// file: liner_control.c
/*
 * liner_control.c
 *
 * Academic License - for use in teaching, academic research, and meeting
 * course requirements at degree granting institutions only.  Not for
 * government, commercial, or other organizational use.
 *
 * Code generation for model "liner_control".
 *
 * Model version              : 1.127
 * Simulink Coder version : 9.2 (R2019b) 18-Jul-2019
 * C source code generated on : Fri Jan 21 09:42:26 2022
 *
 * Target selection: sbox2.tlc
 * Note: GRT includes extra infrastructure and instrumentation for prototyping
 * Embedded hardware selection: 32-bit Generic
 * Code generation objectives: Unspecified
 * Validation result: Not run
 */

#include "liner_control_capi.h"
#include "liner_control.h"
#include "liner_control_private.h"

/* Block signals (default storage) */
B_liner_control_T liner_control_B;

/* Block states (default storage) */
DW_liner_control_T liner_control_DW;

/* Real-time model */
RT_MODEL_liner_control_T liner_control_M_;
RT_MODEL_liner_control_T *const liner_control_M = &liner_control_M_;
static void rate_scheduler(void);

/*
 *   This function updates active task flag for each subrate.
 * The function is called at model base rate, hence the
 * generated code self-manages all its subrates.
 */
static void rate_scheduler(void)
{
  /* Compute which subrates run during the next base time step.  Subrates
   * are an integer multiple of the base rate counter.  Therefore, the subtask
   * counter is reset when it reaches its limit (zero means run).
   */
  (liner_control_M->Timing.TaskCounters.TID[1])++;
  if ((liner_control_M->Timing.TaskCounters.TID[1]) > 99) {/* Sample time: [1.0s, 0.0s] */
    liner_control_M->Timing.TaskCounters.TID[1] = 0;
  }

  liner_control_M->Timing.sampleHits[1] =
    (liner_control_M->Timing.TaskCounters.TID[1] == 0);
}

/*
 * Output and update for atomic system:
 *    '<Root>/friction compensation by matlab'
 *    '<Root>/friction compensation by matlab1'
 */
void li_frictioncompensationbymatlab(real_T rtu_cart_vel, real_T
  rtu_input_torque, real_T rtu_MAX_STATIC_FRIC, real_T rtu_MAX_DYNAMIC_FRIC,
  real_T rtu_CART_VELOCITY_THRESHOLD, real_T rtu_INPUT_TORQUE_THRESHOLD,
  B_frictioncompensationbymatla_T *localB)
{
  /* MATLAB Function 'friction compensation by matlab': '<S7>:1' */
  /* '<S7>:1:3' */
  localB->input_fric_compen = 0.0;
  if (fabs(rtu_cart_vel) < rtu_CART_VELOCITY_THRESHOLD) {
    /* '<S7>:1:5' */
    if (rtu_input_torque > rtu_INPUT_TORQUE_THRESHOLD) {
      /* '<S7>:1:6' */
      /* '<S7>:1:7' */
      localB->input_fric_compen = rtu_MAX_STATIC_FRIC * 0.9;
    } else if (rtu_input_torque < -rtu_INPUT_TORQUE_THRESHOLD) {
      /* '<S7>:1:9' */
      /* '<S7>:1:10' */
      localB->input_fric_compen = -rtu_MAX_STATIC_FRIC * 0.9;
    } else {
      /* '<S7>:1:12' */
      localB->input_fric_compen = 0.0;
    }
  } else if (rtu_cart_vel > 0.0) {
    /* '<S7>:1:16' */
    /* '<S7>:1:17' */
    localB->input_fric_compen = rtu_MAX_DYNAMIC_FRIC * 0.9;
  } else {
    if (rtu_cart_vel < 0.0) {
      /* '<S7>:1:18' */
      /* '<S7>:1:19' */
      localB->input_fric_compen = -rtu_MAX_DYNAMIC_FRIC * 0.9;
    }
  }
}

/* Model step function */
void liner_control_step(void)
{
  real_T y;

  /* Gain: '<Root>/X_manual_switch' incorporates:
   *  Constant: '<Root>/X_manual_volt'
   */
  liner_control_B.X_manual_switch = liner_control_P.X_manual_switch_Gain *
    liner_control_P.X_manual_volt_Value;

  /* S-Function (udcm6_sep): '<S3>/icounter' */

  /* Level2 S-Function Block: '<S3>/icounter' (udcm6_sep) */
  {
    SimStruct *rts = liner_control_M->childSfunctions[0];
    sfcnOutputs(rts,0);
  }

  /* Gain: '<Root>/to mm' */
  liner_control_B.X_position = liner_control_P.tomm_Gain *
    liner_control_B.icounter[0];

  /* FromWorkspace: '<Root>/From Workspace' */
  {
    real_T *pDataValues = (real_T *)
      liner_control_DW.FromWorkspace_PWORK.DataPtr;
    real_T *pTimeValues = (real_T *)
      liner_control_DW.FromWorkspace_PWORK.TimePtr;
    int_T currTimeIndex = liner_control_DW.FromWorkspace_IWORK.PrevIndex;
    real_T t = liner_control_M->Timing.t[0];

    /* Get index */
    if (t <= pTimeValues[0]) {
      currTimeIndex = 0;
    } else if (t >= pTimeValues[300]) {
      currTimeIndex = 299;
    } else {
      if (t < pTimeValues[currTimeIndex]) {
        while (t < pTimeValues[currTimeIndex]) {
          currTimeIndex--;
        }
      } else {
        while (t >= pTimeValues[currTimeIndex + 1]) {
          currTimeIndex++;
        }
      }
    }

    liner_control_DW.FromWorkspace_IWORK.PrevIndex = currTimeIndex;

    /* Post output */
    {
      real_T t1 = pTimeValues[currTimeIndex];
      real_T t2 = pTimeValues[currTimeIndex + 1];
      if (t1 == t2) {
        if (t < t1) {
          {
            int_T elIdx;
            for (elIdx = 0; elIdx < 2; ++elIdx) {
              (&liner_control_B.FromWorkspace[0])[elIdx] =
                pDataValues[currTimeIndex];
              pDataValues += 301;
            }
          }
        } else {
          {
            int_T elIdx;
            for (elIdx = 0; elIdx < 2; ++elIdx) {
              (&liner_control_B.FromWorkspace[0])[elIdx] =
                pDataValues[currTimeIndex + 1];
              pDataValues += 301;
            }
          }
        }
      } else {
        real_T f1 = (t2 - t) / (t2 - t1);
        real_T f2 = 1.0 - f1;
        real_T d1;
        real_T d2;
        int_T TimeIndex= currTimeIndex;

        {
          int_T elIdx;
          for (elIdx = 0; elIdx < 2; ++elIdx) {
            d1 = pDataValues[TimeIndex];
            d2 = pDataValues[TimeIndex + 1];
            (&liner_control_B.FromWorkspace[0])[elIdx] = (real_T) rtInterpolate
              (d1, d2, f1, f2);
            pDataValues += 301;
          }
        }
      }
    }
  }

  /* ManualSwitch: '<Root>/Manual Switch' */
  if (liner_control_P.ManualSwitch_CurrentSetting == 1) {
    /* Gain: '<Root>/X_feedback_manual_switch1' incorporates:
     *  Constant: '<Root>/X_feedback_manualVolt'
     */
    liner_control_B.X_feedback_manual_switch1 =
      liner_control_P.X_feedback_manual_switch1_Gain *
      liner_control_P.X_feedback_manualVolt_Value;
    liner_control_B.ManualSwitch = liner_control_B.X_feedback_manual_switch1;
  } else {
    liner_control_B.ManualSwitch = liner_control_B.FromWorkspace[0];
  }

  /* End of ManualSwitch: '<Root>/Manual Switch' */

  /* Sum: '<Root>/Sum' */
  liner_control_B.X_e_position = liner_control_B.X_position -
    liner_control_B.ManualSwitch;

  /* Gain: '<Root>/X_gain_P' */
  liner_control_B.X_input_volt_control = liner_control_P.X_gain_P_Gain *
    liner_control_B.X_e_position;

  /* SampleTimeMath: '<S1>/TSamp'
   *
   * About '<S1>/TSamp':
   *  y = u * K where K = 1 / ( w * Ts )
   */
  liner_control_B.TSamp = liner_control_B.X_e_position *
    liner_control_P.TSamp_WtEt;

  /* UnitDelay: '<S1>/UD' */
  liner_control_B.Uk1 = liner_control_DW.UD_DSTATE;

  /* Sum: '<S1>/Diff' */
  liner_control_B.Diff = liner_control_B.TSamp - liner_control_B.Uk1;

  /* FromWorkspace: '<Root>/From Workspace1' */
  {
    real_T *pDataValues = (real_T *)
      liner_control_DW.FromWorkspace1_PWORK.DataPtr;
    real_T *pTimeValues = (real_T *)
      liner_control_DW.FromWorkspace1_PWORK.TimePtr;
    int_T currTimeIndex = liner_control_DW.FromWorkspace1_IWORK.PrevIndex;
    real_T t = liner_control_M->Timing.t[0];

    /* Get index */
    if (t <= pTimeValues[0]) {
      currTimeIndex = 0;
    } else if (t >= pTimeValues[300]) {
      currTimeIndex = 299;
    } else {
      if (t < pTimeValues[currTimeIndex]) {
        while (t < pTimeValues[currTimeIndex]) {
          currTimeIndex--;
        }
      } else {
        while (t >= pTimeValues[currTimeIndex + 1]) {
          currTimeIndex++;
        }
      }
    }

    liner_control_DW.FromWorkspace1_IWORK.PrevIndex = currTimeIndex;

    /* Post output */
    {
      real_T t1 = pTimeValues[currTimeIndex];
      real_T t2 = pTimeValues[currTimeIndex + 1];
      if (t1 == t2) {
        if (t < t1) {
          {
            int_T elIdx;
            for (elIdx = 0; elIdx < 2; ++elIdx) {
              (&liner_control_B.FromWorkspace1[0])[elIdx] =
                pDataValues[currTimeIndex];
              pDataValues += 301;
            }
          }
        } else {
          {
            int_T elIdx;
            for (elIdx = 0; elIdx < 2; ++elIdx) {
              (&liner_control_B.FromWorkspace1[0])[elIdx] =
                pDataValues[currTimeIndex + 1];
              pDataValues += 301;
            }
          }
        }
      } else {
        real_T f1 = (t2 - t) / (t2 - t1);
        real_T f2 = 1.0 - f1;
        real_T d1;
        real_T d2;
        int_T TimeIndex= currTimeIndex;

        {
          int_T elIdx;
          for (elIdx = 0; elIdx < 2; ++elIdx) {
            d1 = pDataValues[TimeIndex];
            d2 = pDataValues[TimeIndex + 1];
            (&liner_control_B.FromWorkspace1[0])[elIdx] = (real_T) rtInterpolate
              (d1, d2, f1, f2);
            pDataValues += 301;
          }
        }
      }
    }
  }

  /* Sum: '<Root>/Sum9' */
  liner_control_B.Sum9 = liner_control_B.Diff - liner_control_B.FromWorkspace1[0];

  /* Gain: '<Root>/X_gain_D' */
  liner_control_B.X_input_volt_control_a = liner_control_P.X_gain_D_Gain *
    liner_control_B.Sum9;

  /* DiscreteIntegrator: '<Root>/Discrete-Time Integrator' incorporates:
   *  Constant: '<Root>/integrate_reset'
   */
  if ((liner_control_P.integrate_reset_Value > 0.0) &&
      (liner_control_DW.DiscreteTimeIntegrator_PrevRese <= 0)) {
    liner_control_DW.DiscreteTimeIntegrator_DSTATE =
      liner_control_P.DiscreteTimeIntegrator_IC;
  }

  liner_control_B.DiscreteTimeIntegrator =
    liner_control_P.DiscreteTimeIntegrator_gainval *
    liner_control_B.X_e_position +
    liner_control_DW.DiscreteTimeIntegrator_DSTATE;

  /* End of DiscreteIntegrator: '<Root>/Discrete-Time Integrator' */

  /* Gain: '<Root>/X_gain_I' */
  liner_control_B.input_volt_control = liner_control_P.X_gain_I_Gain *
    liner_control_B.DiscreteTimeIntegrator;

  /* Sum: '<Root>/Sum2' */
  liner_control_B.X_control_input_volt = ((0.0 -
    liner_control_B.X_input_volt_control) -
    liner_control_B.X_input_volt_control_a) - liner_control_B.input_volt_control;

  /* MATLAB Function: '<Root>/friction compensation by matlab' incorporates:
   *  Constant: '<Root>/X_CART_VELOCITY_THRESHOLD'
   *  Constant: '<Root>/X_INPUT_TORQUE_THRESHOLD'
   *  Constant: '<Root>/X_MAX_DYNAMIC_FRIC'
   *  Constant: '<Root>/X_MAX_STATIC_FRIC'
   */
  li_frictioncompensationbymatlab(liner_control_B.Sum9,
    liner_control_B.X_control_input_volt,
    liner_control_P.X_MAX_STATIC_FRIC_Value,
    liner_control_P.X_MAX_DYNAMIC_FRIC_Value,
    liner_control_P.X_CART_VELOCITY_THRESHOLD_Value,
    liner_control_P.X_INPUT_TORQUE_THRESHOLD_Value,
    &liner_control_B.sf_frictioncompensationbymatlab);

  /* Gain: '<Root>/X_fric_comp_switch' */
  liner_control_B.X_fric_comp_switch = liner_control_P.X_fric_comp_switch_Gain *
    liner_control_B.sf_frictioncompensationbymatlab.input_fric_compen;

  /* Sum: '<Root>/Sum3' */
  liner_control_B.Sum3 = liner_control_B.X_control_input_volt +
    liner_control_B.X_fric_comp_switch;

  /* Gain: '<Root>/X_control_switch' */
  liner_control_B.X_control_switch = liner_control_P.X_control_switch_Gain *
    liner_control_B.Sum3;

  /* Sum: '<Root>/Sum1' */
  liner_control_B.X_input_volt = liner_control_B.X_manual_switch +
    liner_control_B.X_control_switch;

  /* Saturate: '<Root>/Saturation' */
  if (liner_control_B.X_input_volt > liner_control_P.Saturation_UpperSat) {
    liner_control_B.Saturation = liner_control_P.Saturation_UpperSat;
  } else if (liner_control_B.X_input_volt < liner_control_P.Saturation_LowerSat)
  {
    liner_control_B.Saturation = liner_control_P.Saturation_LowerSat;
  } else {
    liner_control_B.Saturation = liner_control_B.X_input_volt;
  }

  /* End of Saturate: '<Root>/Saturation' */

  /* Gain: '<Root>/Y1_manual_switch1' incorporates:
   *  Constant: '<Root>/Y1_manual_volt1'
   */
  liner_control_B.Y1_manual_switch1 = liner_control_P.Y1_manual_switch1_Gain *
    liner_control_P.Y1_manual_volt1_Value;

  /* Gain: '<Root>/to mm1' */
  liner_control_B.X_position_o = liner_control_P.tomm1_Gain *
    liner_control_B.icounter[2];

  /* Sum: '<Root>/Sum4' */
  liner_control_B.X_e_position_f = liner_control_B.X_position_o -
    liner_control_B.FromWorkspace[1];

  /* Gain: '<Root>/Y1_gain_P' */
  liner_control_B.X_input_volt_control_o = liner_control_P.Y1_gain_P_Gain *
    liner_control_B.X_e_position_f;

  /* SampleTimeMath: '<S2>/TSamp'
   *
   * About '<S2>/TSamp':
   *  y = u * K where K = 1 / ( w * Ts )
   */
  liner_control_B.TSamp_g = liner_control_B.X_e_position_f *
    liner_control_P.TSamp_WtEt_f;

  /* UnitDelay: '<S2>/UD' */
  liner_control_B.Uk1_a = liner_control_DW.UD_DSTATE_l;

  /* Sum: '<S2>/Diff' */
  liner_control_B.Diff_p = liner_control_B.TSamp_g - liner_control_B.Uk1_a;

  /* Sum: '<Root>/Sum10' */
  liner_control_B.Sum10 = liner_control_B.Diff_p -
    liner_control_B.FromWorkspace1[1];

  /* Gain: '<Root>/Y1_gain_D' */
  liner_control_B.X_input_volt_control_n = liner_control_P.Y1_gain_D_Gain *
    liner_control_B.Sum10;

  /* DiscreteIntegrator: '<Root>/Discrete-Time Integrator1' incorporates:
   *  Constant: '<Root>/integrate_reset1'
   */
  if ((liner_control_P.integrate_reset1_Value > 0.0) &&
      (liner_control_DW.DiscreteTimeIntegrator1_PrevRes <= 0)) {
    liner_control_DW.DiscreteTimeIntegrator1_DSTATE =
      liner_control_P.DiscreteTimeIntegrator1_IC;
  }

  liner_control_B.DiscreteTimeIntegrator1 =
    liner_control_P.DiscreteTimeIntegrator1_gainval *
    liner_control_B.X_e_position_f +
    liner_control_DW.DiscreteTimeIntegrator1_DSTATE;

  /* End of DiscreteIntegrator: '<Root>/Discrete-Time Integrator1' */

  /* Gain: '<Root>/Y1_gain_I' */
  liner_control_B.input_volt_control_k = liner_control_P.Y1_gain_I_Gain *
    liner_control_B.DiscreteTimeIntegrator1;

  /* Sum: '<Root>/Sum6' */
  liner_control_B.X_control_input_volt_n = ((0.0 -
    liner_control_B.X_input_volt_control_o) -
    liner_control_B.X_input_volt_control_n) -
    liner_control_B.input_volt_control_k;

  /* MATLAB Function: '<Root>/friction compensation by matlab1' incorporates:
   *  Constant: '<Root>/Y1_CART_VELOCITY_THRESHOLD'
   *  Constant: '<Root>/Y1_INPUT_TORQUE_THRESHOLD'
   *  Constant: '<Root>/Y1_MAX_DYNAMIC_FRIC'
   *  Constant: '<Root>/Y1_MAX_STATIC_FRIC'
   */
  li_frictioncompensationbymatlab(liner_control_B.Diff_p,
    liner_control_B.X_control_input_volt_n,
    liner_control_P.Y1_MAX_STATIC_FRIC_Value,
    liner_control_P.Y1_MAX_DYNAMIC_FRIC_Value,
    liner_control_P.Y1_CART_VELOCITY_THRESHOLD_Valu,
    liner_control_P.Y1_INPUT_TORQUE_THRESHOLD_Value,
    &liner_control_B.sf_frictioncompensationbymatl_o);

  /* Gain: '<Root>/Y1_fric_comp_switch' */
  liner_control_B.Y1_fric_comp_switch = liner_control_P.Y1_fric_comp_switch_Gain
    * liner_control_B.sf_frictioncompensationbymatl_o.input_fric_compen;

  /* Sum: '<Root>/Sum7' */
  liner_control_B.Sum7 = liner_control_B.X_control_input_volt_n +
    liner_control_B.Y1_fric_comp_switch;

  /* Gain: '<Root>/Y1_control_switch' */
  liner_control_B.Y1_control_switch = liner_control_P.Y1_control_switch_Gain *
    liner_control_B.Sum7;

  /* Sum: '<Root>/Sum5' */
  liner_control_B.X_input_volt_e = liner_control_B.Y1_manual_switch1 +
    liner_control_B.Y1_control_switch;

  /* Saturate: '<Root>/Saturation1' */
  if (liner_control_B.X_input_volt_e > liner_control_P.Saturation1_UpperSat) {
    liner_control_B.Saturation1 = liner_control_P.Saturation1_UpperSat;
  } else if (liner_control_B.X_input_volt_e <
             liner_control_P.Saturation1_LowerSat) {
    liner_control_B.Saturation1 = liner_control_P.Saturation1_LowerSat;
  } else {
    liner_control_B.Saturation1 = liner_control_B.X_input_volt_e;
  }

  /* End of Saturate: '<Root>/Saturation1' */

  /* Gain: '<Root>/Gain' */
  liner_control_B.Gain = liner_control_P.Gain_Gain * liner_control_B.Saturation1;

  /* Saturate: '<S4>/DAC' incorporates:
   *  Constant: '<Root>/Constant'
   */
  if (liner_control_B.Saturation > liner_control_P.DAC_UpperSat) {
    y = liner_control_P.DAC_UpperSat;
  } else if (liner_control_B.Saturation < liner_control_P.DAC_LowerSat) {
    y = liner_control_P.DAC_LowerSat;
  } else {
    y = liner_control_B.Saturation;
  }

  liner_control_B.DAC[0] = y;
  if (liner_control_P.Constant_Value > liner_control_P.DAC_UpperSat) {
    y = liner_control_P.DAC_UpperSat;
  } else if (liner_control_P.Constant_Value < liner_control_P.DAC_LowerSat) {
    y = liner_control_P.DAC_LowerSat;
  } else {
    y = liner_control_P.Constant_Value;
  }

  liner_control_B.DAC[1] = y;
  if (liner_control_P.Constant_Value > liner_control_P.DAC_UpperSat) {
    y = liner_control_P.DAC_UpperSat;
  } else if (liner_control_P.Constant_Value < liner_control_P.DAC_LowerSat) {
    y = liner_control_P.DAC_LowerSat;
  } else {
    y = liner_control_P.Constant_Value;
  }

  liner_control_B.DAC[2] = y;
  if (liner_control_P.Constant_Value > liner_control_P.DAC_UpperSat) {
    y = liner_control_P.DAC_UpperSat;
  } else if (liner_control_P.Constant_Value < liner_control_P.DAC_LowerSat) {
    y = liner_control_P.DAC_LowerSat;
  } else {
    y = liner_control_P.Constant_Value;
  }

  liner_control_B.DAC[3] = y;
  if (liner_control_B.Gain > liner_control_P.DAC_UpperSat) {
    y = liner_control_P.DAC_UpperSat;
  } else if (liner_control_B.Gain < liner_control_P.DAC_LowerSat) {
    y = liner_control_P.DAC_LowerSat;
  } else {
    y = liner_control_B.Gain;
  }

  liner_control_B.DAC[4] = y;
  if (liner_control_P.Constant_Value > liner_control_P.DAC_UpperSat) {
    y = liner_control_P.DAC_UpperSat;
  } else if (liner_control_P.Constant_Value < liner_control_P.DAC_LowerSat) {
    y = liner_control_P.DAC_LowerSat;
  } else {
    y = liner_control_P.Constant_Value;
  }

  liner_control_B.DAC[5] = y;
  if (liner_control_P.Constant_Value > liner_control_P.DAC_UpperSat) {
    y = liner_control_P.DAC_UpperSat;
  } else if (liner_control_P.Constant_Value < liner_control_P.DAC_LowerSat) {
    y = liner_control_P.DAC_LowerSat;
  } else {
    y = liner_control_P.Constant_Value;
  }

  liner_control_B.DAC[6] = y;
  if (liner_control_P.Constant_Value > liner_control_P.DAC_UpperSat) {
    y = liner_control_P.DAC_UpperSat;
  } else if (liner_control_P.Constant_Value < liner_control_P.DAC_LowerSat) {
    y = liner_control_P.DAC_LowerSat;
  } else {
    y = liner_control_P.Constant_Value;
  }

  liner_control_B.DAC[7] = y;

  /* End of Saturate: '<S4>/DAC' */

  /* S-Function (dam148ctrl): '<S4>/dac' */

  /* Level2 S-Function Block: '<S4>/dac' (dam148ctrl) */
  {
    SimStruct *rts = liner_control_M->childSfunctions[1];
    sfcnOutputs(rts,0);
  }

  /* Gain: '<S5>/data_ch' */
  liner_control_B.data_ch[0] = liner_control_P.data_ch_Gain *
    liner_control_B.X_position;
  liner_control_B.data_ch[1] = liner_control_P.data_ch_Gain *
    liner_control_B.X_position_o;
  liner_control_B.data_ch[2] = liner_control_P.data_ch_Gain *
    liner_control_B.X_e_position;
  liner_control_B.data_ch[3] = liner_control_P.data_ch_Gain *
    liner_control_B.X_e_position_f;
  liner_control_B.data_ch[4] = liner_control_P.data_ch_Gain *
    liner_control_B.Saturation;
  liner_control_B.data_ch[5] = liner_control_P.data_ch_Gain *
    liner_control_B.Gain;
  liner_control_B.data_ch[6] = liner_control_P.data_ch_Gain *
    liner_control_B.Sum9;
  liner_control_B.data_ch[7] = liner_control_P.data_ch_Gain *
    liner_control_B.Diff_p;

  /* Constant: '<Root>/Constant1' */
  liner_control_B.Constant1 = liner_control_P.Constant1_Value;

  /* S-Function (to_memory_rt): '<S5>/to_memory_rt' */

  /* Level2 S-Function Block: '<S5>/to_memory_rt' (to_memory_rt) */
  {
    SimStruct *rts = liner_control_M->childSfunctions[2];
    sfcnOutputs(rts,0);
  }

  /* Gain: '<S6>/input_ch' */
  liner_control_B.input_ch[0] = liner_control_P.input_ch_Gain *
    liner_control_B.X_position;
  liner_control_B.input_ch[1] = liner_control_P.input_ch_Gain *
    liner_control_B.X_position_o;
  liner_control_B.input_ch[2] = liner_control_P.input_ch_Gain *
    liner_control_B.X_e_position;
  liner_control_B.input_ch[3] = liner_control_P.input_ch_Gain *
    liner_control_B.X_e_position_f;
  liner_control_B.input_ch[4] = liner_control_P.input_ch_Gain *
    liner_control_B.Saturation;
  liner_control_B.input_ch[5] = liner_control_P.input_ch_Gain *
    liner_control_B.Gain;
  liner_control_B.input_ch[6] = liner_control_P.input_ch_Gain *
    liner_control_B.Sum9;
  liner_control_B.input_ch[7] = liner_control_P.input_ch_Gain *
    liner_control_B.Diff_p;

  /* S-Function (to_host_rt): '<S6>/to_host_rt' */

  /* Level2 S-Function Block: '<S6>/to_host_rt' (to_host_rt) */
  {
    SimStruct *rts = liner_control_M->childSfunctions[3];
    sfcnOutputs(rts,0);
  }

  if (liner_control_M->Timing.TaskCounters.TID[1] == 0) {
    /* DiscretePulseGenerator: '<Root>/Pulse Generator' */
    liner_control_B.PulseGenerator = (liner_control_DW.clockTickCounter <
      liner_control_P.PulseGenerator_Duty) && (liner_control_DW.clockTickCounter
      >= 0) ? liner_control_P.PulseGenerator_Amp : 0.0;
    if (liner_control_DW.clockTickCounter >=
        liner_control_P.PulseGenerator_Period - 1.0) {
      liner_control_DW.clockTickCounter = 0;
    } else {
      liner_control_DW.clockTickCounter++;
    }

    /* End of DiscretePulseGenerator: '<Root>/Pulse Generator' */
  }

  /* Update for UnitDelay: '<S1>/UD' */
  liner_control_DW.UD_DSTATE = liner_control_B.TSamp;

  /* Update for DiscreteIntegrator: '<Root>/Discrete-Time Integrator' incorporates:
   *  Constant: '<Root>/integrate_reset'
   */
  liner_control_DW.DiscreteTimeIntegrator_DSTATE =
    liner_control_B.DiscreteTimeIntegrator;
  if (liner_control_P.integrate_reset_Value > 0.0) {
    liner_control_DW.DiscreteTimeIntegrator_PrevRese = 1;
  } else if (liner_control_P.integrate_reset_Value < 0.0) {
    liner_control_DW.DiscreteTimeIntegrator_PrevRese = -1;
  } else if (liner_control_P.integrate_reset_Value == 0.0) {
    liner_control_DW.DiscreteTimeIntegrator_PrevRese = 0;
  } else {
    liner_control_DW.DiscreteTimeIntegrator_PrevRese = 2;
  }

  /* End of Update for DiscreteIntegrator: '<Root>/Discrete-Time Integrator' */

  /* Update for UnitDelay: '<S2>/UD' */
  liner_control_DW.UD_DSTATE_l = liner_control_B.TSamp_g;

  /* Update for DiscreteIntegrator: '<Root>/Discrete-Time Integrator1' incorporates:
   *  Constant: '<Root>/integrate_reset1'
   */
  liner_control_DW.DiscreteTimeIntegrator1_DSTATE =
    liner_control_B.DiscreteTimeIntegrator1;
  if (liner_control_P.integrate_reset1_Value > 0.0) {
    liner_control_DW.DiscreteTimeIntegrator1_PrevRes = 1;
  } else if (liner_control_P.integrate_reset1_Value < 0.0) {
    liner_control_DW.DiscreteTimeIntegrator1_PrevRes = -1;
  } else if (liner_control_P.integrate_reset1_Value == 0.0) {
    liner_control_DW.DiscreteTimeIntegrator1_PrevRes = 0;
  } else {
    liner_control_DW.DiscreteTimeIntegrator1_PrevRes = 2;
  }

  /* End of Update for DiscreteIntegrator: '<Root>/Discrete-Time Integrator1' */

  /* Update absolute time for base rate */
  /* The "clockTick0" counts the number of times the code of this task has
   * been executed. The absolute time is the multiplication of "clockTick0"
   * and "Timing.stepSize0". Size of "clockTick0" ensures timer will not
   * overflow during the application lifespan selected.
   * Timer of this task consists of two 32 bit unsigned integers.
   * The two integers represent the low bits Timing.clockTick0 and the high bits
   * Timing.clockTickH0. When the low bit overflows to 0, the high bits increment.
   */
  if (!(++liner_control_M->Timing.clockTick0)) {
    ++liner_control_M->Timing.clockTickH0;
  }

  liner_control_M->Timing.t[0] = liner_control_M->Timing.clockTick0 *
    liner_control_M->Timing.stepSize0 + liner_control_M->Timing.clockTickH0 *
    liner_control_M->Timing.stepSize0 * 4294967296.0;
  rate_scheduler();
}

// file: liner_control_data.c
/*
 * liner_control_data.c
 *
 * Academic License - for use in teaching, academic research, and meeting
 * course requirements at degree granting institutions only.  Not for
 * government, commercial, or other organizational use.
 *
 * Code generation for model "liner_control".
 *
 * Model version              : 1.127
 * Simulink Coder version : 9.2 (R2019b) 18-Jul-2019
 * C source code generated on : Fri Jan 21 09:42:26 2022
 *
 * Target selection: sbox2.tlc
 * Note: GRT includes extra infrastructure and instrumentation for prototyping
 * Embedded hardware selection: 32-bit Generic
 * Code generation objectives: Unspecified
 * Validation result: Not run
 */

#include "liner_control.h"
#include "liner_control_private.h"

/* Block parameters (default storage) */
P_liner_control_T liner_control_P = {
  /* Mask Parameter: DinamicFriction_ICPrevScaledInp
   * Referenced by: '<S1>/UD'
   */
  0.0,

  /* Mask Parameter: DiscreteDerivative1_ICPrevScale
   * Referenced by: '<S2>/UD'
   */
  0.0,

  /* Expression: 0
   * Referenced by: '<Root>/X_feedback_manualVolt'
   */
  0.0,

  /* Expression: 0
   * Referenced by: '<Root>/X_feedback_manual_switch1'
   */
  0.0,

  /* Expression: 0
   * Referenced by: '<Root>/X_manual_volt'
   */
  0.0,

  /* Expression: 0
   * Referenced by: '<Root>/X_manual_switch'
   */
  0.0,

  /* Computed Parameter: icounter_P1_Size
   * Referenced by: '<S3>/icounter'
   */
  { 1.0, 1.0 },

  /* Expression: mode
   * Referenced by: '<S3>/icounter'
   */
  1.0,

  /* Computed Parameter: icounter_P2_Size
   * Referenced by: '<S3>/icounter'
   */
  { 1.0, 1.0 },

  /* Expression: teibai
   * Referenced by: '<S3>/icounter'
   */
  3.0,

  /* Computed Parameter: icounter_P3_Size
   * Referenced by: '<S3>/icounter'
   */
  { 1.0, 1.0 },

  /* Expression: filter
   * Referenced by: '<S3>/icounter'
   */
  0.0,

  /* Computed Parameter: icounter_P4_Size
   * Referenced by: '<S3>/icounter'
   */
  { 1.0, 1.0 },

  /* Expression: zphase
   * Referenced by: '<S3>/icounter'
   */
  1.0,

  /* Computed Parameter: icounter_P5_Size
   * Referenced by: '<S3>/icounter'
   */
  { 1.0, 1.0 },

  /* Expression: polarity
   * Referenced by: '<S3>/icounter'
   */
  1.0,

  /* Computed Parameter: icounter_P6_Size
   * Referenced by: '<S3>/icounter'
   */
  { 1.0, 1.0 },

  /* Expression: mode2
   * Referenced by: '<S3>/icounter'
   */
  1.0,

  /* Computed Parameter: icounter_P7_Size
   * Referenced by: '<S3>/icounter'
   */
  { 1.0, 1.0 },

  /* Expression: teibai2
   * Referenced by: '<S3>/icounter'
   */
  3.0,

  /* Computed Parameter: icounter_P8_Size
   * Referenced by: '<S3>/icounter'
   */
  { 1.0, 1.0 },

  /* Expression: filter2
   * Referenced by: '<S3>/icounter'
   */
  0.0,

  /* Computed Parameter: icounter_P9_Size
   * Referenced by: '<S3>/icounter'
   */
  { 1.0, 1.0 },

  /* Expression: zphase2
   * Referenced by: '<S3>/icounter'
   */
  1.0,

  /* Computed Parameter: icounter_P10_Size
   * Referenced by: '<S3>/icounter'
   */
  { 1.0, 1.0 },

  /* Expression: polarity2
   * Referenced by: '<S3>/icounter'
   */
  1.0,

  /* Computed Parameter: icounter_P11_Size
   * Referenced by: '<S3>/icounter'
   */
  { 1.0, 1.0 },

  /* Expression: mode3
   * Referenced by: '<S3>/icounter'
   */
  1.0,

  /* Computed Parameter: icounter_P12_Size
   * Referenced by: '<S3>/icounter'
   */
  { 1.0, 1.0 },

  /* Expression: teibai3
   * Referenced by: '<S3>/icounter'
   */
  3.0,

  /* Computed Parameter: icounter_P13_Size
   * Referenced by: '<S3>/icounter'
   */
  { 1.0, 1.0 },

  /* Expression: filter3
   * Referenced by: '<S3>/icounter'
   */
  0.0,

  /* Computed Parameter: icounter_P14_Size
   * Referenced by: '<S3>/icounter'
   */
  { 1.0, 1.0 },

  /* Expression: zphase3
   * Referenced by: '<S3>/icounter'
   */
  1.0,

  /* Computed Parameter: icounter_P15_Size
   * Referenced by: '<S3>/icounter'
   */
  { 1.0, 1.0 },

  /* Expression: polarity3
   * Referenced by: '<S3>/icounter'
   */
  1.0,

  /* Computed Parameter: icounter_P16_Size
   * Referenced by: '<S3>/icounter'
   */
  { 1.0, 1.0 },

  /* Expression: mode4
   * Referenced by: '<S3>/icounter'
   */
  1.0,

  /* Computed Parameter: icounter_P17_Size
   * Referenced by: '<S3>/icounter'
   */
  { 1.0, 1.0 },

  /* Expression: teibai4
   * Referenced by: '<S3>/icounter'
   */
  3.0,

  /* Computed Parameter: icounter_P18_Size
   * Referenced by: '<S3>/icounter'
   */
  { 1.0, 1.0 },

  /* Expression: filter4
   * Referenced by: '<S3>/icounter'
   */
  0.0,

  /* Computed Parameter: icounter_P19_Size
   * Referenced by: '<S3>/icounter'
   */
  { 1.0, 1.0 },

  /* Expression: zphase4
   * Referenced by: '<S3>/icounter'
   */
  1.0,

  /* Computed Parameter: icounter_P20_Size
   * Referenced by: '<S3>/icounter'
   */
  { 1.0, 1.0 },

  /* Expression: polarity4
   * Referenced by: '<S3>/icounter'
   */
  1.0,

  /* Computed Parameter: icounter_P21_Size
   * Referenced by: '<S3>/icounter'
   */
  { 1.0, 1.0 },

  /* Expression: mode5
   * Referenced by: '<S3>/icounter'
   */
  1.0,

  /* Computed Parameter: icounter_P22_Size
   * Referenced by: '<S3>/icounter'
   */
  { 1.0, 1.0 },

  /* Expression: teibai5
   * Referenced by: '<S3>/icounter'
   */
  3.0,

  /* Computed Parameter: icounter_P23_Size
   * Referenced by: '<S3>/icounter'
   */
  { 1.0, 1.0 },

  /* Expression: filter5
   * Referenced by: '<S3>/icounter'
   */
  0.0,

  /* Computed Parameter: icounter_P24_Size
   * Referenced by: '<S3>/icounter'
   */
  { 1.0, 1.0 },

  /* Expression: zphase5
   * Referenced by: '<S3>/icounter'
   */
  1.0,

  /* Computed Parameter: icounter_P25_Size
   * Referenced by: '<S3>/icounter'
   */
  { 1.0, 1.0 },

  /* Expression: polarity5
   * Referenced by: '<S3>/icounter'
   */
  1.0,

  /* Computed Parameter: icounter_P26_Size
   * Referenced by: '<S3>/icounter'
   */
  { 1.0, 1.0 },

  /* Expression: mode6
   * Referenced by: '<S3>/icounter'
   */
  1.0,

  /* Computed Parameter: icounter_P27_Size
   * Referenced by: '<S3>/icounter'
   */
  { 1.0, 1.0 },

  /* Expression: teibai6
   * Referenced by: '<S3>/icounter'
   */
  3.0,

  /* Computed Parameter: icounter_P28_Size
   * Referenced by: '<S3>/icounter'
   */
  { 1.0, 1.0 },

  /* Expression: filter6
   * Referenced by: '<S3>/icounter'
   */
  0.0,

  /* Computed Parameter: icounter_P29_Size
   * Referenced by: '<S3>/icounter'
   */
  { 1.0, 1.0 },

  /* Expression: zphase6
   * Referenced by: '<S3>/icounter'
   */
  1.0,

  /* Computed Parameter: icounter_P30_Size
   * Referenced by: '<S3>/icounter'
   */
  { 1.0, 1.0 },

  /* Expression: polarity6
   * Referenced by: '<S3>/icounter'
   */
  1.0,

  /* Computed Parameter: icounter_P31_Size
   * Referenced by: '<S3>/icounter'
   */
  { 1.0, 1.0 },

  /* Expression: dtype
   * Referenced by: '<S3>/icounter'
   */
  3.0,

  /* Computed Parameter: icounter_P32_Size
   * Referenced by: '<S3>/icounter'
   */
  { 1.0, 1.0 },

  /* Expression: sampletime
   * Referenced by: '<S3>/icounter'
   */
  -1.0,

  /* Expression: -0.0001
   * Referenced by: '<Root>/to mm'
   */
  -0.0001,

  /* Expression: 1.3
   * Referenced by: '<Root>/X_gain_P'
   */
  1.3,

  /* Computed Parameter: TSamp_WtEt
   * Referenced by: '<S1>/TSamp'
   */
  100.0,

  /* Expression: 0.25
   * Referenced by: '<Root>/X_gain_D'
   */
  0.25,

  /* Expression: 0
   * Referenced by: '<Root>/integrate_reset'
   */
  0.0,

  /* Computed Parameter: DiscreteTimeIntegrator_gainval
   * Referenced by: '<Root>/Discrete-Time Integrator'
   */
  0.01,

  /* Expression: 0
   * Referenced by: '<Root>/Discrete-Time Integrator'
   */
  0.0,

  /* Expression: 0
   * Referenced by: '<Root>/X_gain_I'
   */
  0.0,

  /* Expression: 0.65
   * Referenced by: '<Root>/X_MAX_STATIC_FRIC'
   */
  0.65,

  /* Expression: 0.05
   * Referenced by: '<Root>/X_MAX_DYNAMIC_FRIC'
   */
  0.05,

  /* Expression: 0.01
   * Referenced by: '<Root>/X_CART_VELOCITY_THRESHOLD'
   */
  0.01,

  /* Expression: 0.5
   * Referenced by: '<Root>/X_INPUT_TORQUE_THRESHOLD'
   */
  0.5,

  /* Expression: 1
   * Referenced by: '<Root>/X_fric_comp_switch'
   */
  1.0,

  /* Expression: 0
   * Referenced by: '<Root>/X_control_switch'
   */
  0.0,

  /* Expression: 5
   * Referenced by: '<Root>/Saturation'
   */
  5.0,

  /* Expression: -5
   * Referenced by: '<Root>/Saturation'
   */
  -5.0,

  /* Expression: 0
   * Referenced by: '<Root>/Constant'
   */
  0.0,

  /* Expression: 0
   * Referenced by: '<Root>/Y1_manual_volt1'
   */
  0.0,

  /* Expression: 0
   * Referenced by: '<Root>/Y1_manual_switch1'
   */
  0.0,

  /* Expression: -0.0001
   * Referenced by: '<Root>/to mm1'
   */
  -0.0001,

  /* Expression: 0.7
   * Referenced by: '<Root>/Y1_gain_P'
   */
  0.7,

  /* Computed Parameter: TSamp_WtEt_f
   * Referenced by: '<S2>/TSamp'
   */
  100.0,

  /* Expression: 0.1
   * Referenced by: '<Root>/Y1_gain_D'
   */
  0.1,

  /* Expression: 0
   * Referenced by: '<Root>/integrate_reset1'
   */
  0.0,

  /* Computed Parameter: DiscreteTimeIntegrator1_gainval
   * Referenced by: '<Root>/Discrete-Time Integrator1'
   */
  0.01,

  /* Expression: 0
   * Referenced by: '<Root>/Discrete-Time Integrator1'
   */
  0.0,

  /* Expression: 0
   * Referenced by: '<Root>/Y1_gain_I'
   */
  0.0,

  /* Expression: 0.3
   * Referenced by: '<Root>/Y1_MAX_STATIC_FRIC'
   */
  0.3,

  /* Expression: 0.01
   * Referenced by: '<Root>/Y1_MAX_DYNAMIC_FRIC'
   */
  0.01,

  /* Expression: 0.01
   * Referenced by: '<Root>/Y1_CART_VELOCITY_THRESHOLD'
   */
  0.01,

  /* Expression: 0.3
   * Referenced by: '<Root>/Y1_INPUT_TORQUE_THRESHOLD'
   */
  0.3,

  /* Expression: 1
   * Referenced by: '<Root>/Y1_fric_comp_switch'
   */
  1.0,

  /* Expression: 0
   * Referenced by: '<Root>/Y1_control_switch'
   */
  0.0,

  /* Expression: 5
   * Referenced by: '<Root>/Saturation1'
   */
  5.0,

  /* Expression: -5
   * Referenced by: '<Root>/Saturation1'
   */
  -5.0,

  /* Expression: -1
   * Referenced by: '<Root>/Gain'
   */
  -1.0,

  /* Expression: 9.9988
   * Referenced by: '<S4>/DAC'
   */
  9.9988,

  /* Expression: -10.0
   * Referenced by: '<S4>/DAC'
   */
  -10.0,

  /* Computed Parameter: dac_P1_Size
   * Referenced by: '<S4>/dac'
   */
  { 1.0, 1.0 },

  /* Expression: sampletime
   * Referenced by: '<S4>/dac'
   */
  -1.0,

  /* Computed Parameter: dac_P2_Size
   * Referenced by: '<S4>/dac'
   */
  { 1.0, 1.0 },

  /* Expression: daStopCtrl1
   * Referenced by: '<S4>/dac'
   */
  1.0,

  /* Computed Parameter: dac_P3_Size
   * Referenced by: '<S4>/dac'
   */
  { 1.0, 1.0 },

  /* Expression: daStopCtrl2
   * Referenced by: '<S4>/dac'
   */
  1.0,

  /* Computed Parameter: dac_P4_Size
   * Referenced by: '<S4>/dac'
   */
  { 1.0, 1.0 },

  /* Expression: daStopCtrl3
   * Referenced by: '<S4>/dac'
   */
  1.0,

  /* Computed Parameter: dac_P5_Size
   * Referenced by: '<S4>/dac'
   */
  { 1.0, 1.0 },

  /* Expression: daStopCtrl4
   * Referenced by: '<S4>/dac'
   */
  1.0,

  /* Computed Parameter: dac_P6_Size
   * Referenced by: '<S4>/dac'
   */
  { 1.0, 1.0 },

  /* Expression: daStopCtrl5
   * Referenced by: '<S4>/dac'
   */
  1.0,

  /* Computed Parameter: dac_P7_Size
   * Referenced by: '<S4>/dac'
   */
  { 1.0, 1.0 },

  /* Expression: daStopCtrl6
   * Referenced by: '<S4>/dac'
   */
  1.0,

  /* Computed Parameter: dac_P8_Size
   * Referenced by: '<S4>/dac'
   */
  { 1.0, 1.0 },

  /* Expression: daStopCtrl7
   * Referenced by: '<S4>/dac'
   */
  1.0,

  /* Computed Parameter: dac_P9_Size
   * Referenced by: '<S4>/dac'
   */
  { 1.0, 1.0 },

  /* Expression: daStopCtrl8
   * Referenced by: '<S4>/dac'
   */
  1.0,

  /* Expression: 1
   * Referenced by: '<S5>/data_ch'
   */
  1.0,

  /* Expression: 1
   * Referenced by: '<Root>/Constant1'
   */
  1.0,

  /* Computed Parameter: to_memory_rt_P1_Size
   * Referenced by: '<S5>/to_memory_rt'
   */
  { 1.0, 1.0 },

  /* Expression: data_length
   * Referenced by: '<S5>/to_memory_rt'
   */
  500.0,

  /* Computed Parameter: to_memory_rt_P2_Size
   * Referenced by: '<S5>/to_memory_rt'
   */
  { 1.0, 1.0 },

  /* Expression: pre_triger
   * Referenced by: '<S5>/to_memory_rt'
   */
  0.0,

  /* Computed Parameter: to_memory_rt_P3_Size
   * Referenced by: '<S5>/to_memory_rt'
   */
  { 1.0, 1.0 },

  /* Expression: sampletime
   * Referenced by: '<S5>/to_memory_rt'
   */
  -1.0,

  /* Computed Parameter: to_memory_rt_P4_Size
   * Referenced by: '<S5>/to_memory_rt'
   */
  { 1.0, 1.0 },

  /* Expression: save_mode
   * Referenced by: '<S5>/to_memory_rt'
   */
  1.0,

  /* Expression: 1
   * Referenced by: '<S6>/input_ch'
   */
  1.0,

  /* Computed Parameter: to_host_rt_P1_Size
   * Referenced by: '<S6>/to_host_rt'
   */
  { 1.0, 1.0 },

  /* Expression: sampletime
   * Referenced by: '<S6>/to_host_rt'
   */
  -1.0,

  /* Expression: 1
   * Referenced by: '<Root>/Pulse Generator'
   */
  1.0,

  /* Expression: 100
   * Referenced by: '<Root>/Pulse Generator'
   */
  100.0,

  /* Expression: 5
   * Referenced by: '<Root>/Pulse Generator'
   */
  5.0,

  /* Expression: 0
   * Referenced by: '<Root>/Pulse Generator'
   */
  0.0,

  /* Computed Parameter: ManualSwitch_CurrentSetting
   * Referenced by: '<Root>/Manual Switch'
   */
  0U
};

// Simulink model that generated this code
simulink model "liner_control"  (R2019b)
settings: Solver=FixedStepAuto  StartTime=0.0  StopTime=100  FixedStep=0.01  RelTol=1e-3
undefined symbols (not defined in the file or in its folder): DiscIntNeverNeededParam
libraries: sbox2 x4, simulink x2

== system liner_control ==
  note: y velocity
  note: x velocity
  note: y input
  note: x input
  note: Input Trajectory data
  note: x signal
  note: y1-err
  note: x-err
  note: Subsystem2
  note: Subsystem
  note: y signal
  note: Input Trajectory data
  note: x signal
  note: y signal
  Constant : Constant  Value=0
  Constant1 : Constant
  Demux : Demux  Outputs=6
  Demux1 : Demux  Outputs=2
  Demux2 : Demux  Outputs=2
  DinamicFriction : simulink/Discrete/Discrete Derivative  gainval=1.0  ICPrevScaledInput=0.0  OutMin=[]  OutMax=[]  OutDataType=fixdt(1, 16)  OutScaling=2^-10  DoSatur=off
  Discrete Derivative1 : simulink/Discrete/Discrete Derivative  gainval=1.0  ICPrevScaledInput=0.0  OutMin=[]  OutMax=[]  OutDataType=fixdt(1, 16)  OutScaling=2^-10  DoSatur=off
  Discrete-Time Integrator : DiscreteIntegrator  IntegratorMethod=Integration: Backward Euler  ExternalReset=rising  SampleTime=-1  ICPrevOutput=DiscIntNeverNeededParam  ICPrevScaledInput=DiscIntNeverNeededParam
  Discrete-Time Integrator1 : DiscreteIntegrator  IntegratorMethod=Integration: Backward Euler  ExternalReset=rising  SampleTime=-1  ICPrevOutput=DiscIntNeverNeededParam  ICPrevScaledInput=DiscIntNeverNeededParam
  From Workspace : FromWorkspace  VariableName=inputPosition  SampleTime=0.01
  From Workspace1 : FromWorkspace  VariableName=inputVelocity  SampleTime=0.01
  Gain : Gain  Gain=-1
  Manual Switch : ManualSwitch  CurrentSetting=0
  Mux : Mux  Inputs=8
  Mux1 : Mux  Inputs=8
  Pulse Generator : DiscretePulseGenerator  Period=100  PulseWidth=5
  SBOX2_CNT6 : sbox2/Digital I//O Devices/SBOX2_CNT6  mode=2相パルス  teibai=x4  filter=off  zphase=動作なし  polarity=正論理 (high active)  mode2=2相パルス  teibai2=x4  filter2=off  zphase2=動作なし  polarity2=正論理 (high active)  mode3=2相パルス  teibai3=x4  filter3=off  zphase3=動作なし  polarity3=正論理 (high active)  mode4=2相パルス  teibai4=x4  filter4=off  zphase4=動作なし  polarity4=正論理 (high active)  mode5=2相パルス  teibai5=x4  filter5=off  zphase5=動作なし  polarity5=正論理 (high active)  mode6=2相パルス  teibai6=x4  filter6=off  zphase6=動作なし  polarity6=正論理 (high active)  dtype=FLOATING POINT  sampletime=-1
  "SBOX2_DAM148 " : sbox2/Analog I//O Devices/SBOX2_DAM148_NET  daStopCtrl1=DA出力継続  daStopCtrl2=DA出力継続  daStopCtrl3=DA出力継続  daStopCtrl4=DA出力継続  daStopCtrl5=DA出力継続  daStopCtrl6=DA出力継続  daStopCtrl7=DA出力継続  daStopCtrl8=DA出力継続  sampletime=-1
  SBOX2_DATA_SAVE_NET : sbox2/Network Data Save Devices/SBOX2_DATA_SAVE_NET  save_mode=ホストアプリケーション指示によるトリガ待ち  data_length=500  pre_triger=0  sampletime=-1
  SBOX2_GRAPH_MONITOR : sbox2/Network Data Save Devices/SBOX2_GRAPH_MONITOR  sampletime=-1
  Saturation : Saturate  UpperLimit=5  LowerLimit=-5
  Saturation1 : Saturate  UpperLimit=5  LowerLimit=-5
  Sum : Sum  Inputs=|+-
  Sum1 : Sum  Inputs=++|
  Sum10 : Sum  Inputs=-+|
  Sum2 : Sum  Inputs=---
  Sum3 : Sum  Inputs=|++
  Sum4 : Sum  Inputs=-+|
  Sum5 : Sum  Inputs=++|
  Sum6 : Sum  Inputs=---
  Sum7 : Sum  Inputs=|++
  Sum9 : Sum  Inputs=|+-
  X_CART_VELOCITY_THRESHOLD : Constant  Value=0.01
  X_INPUT_TORQUE_THRESHOLD : Constant  Value=0.5
  X_MAX_DYNAMIC_FRIC : Constant  Value=0.05
  X_MAX_STATIC_FRIC : Constant  Value=0.65
  X_control_switch : Gain  Gain=0
  X_feedback_manualVolt : Constant  Value=0
  X_feedback_manual_switch1 : Gain  Gain=0
  X_fric_comp_switch : Gain
  X_gain_D : Gain  Gain=0.25
  X_gain_I : Gain  Gain=0
  X_gain_P : Gain  Gain=1.3
  X_manual_switch : Gain  Gain=0
  X_manual_volt : Constant  Value=0
  Y1_CART_VELOCITY_THRESHOLD : Constant  Value=0.01
  Y1_INPUT_TORQUE_THRESHOLD : Constant  Value=0.3
  Y1_MAX_DYNAMIC_FRIC : Constant  Value=0.01
  Y1_MAX_STATIC_FRIC : Constant  Value=0.3
  Y1_control_switch : Gain  Gain=0
  Y1_fric_comp_switch : Gain
  Y1_gain_D : Gain  Gain=0.1
  Y1_gain_I : Gain  Gain=0
  Y1_gain_P : Gain  Gain=0.7
  Y1_manual_switch1 : Gain  Gain=0
  Y1_manual_volt1 : Constant  Value=0
  friction compensation by matlab : MATLAB Function  TreatAsAtomicUnit=on
  friction compensation by matlab1 : MATLAB Function  TreatAsAtomicUnit=on
  integrate_reset : Constant  Value=0
  integrate_reset1 : Constant  Value=0
  to mm : Gain  Gain=-0.0001
  to mm1 : Gain  Gain=-0.0001
  wires:
  SBOX2_CNT6/1 -> Demux/1
  Mux/1 -> "SBOX2_DAM148 "/1
  Constant/1 -> Mux/7, Mux/3, Mux/2, Mux/4, Mux/6, Mux/8
  Saturation/1 -> Mux1/5, Mux/1
  Saturation1/1 -> Gain/1
  X_fric_comp_switch/1 -> Sum3/2
  Sum3/1 -> X_control_switch/1
  X_manual_volt/1 -> X_manual_switch/1
  integrate_reset/1 -> Discrete-Time Integrator/2
  X_CART_VELOCITY_THRESHOLD/1 -> friction compensation by matlab/5(CART_VELOCITY_THRESHOLD)
  X_MAX_DYNAMIC_FRIC/1 -> friction compensation by matlab/4(MAX_DYNAMIC_FRIC)
  to mm/1 -> Mux1/1, Sum/1  "X_position"
  X_gain_D/1 -> Sum2/2  "X_input_volt_control"
  X_MAX_STATIC_FRIC/1 -> friction compensation by matlab/3(MAX_STATIC_FRIC)
  friction compensation by matlab/1(input_fric_compen) -> X_fric_comp_switch/1
  X_manual_switch/1 -> Sum1/1
  X_INPUT_TORQUE_THRESHOLD/1 -> friction compensation by matlab/6(INPUT_TORQUE_THRESHOLD)
  X_gain_I/1 -> Sum2/3  "input_volt_control"
  Sum/1 -> Mux1/3, DinamicFriction/1, Discrete-Time Integrator/1, X_gain_P/1  "X_e_position"
  X_gain_P/1 -> Sum2/1  "X_input_volt_control"
  Discrete-Time Integrator/1 -> X_gain_I/1
  Sum2/1 -> Sum3/1, friction compensation by matlab/2(input_torque)  "X_control_input_volt"
  Demux/1 -> to mm/1
  Sum9/1 -> friction compensation by matlab/1(cart_vel), Mux1/7, X_gain_D/1
  Sum1/1 -> Saturation/1  "X_input_volt"
  Y1_fric_comp_switch/1 -> Sum7/2
  Sum7/1 -> Y1_control_switch/1
  Y1_manual_volt1/1 -> Y1_manual_switch1/1
  integrate_reset1/1 -> Discrete-Time Integrator1/2
  Y1_CART_VELOCITY_THRESHOLD/1 -> friction compensation by matlab1/5(CART_VELOCITY_THRESHOLD)
  Y1_MAX_DYNAMIC_FRIC/1 -> friction compensation by matlab1/4(MAX_DYNAMIC_FRIC)
  to mm1/1 -> Sum4/2, Mux1/2  "X_position"
  Y1_gain_D/1 -> Sum6/2  "X_input_volt_control"
  Y1_MAX_STATIC_FRIC/1 -> friction compensation by matlab1/3(MAX_STATIC_FRIC)
  friction compensation by matlab1/1(input_fric_compen) -> Y1_fric_comp_switch/1
  Y1_manual_switch1/1 -> Sum5/1
  Y1_INPUT_TORQUE_THRESHOLD/1 -> friction compensation by matlab1/6(INPUT_TORQUE_THRESHOLD)
  Y1_gain_I/1 -> Sum6/3  "input_volt_control"
  Sum4/1 -> Discrete-Time Integrator1/1, Discrete Derivative1/1, Mux1/4, Y1_gain_P/1  "X_e_position"
  Y1_gain_P/1 -> Sum6/1  "X_input_volt_control"
  Discrete-Time Integrator1/1 -> Y1_gain_I/1
  Sum6/1 -> Sum7/1, friction compensation by matlab1/2(input_torque)  "X_control_input_volt"
  Demux/3 -> to mm1/1
  Discrete Derivative1/1 -> Sum10/2, friction compensation by matlab1/1(cart_vel), Mux1/8
  Sum5/1 -> Saturation1/1  "X_input_volt"
  Y1_control_switch/1 -> Sum5/2
  X_control_switch/1 -> Sum1/2
  Gain/1 -> Mux/5, Mux1/6
  From Workspace/1 -> Demux1/1
  Demux1/2 -> Sum4/1
  X_feedback_manual_switch1/1 -> Manual Switch/1
  X_feedback_manualVolt/1 -> X_feedback_manual_switch1/1
  Manual Switch/1 -> Sum/2
  Demux1/1 -> Manual Switch/2
  Mux1/1 -> SBOX2_GRAPH_MONITOR/1, SBOX2_DATA_SAVE_NET/1
  Constant1/1 -> SBOX2_DATA_SAVE_NET/2
  DinamicFriction/1 -> Sum9/1
  Demux2/1 -> Sum9/2
  From Workspace1/1 -> Demux2/1
  Demux2/2 -> Sum10/1
  Sum10/1 -> Y1_gain_D/1

== matlab function liner_control/friction compensation by matlab ==
function input_fric_compen = fcn(cart_vel, input_torque, MAX_STATIC_FRIC, MAX_DYNAMIC_FRIC, CART_VELOCITY_THRESHOLD, INPUT_TORQUE_THRESHOLD)

input_fric_compen = zeros(1);

if abs(cart_vel) < CART_VELOCITY_THRESHOLD
    if input_torque > INPUT_TORQUE_THRESHOLD
        input_fric_compen = MAX_STATIC_FRIC * 0.9;
    else
        if input_torque < -INPUT_TORQUE_THRESHOLD
            input_fric_compen = - MAX_STATIC_FRIC * 0.9;
        else
            input_fric_compen = 0.0;
        end
    end
else
    if cart_vel > 0.0
        input_fric_compen = MAX_DYNAMIC_FRIC * 0.9;
    elseif cart_vel < 0.0
        input_fric_compen = - MAX_DYNAMIC_FRIC * 0.9;
    end
end

end

== matlab function liner_control/friction compensation by matlab1 ==
function input_fric_compen = fcn(cart_vel, input_torque, MAX_STATIC_FRIC, MAX_DYNAMIC_FRIC, CART_VELOCITY_THRESHOLD, INPUT_TORQUE_THRESHOLD)

input_fric_compen = zeros(1);

if abs(cart_vel) < CART_VELOCITY_THRESHOLD
    if input_torque > INPUT_TORQUE_THRESHOLD
        input_fric_compen = MAX_STATIC_FRIC * 0.9;
    else
        if input_torque < -INPUT_TORQUE_THRESHOLD
            input_fric_compen = - MAX_STATIC_FRIC * 0.9;
        else
            input_fric_compen = 0.0;
        end
    end
else
    if cart_vel > 0.0
        input_fric_compen = MAX_DYNAMIC_FRIC * 0.9;
    elseif cart_vel < 0.0
        input_fric_compen = - MAX_DYNAMIC_FRIC * 0.9;
    end
end

end
